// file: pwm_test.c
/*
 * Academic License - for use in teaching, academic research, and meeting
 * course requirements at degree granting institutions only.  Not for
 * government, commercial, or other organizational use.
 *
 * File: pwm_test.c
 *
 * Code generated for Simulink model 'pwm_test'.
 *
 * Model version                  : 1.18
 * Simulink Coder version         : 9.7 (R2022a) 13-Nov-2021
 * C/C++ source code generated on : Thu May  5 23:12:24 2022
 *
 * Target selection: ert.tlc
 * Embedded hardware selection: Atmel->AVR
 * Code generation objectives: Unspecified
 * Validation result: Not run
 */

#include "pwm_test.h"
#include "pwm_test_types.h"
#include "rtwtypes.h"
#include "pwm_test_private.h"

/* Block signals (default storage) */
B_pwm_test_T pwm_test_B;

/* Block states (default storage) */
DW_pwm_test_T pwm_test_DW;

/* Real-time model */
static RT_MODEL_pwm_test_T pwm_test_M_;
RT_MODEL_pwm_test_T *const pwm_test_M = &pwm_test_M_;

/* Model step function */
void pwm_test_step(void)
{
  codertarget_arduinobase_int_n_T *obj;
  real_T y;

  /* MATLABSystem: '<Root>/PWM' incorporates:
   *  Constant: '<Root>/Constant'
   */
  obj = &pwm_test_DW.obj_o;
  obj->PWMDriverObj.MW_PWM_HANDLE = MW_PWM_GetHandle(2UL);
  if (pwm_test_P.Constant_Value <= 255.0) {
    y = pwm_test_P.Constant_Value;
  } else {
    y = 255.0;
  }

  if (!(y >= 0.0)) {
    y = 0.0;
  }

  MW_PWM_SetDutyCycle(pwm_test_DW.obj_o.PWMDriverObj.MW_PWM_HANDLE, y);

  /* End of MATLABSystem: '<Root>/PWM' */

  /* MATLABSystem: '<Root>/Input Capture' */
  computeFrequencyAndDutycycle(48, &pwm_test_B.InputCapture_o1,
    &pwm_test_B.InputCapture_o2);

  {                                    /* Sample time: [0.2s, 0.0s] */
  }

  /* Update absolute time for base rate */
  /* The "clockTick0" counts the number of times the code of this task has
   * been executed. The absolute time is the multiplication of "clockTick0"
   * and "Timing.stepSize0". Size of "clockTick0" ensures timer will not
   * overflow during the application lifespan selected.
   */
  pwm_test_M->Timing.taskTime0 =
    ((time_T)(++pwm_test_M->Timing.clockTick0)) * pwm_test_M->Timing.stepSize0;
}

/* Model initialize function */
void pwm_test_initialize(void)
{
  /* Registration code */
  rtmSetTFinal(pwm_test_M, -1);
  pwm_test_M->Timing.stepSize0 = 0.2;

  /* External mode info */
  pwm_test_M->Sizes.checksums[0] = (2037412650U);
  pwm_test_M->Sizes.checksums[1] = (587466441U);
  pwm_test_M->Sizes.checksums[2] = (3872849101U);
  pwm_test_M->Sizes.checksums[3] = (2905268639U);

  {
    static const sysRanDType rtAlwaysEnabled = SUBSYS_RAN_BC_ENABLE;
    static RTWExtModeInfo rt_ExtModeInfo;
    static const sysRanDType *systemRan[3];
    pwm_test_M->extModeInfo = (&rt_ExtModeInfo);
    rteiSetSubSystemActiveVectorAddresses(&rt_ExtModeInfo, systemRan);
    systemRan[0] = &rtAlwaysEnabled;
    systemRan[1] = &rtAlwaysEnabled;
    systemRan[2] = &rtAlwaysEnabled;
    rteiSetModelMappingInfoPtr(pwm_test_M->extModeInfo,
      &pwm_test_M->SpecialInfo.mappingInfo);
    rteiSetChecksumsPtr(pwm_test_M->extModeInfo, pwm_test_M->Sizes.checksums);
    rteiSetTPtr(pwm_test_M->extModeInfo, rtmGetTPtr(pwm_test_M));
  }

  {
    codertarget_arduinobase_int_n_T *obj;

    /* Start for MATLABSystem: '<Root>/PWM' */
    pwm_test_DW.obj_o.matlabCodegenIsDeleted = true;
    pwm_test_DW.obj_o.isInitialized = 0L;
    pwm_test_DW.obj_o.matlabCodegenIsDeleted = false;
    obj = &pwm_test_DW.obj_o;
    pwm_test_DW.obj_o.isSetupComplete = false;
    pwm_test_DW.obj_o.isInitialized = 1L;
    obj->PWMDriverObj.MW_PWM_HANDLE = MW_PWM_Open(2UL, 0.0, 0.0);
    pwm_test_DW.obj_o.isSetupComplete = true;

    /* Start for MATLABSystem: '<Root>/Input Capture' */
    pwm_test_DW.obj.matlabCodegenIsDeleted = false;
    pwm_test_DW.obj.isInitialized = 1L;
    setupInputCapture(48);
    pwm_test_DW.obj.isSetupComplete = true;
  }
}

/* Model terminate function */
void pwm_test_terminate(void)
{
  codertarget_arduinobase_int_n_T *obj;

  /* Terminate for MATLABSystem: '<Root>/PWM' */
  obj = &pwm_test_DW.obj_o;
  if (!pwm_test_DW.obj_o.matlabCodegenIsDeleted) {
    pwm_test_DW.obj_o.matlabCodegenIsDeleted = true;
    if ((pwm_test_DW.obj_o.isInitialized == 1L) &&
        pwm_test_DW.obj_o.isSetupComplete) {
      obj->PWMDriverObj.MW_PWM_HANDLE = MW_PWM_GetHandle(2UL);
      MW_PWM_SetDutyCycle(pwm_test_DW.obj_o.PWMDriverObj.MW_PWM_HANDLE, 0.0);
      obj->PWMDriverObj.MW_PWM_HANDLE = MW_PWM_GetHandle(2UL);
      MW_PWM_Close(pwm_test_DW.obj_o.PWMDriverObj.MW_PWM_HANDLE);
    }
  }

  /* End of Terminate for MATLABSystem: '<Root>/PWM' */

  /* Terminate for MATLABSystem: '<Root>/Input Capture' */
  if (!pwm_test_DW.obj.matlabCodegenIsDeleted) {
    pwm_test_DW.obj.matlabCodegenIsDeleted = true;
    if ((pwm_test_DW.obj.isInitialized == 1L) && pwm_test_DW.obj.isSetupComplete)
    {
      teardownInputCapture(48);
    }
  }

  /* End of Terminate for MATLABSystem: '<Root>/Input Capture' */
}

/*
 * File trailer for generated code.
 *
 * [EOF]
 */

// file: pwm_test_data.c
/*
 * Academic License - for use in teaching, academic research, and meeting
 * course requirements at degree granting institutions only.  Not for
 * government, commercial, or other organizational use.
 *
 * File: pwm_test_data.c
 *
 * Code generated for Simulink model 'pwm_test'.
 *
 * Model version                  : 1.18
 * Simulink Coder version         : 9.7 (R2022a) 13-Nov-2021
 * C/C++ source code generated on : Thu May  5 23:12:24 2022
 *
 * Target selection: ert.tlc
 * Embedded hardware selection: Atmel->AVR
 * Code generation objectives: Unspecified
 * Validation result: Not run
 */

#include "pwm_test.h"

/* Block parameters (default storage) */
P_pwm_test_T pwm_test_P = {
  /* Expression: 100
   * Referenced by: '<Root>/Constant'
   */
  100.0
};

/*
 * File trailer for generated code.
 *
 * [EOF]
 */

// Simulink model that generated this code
simulink model "pwm_test"  (R2022a)
settings: Solver=FixedStepAuto  StartTime=0.0  StopTime=inf  RelTol=1e-3  EnableMultiTasking=on
libraries: arduinolib x2

== system pwm_test ==
  note: PWM Source
  Constant : Constant  Value=100
  Display : Display
  Display1 : Display
  Input Capture : arduinolib/Input Capture  InputCapturePinNumber=48  SampleTime=0.0001
  PWM : arduinolib/PWM  pinNumber=2  frequencyType=Default  desiredFrequency=1000  achievableFrequency=10
  wires:
  Constant/1 -> PWM/1
  Input Capture/2 -> Display/1
  Input Capture/1 -> Display1/1
